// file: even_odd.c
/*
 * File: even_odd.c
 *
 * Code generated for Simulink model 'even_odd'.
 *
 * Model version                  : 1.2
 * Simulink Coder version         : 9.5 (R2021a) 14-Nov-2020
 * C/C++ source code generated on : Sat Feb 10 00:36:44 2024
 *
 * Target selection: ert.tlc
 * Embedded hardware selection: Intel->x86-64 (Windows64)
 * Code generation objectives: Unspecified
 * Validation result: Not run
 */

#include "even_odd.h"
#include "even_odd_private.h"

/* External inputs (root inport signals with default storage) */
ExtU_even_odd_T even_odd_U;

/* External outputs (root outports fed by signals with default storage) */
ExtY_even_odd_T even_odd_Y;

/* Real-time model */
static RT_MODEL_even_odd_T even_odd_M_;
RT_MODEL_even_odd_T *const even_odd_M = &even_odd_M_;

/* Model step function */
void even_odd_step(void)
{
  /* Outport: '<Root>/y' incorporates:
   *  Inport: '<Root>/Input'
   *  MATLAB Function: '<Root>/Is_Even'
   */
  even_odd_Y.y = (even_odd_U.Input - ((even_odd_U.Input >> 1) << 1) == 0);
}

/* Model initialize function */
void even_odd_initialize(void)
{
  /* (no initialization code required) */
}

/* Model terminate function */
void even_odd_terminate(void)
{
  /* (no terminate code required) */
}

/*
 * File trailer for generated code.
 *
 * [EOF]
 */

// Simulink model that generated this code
simulink model "even_odd"  (R2021a)
settings: Solver=FixedStepDiscrete  StartTime=0.0  StopTime=10.0  RelTol=1e-3

== system even_odd ==
  Input : Inport  OutDataTypeStr=int32
  Is_Even : MATLAB Function  TreatAsAtomicUnit=on
  y : Outport
  wires:
  Input/1 -> Is_Even/1(Num)
  Is_Even/1(y) -> y/1

== matlab function even_odd/Is_Even ==
function y = fcn(Num)
if mod(Num, 2) == 0
    y = 1;
    % means number is even
else
    y = 0;
    % means number is odd
end
